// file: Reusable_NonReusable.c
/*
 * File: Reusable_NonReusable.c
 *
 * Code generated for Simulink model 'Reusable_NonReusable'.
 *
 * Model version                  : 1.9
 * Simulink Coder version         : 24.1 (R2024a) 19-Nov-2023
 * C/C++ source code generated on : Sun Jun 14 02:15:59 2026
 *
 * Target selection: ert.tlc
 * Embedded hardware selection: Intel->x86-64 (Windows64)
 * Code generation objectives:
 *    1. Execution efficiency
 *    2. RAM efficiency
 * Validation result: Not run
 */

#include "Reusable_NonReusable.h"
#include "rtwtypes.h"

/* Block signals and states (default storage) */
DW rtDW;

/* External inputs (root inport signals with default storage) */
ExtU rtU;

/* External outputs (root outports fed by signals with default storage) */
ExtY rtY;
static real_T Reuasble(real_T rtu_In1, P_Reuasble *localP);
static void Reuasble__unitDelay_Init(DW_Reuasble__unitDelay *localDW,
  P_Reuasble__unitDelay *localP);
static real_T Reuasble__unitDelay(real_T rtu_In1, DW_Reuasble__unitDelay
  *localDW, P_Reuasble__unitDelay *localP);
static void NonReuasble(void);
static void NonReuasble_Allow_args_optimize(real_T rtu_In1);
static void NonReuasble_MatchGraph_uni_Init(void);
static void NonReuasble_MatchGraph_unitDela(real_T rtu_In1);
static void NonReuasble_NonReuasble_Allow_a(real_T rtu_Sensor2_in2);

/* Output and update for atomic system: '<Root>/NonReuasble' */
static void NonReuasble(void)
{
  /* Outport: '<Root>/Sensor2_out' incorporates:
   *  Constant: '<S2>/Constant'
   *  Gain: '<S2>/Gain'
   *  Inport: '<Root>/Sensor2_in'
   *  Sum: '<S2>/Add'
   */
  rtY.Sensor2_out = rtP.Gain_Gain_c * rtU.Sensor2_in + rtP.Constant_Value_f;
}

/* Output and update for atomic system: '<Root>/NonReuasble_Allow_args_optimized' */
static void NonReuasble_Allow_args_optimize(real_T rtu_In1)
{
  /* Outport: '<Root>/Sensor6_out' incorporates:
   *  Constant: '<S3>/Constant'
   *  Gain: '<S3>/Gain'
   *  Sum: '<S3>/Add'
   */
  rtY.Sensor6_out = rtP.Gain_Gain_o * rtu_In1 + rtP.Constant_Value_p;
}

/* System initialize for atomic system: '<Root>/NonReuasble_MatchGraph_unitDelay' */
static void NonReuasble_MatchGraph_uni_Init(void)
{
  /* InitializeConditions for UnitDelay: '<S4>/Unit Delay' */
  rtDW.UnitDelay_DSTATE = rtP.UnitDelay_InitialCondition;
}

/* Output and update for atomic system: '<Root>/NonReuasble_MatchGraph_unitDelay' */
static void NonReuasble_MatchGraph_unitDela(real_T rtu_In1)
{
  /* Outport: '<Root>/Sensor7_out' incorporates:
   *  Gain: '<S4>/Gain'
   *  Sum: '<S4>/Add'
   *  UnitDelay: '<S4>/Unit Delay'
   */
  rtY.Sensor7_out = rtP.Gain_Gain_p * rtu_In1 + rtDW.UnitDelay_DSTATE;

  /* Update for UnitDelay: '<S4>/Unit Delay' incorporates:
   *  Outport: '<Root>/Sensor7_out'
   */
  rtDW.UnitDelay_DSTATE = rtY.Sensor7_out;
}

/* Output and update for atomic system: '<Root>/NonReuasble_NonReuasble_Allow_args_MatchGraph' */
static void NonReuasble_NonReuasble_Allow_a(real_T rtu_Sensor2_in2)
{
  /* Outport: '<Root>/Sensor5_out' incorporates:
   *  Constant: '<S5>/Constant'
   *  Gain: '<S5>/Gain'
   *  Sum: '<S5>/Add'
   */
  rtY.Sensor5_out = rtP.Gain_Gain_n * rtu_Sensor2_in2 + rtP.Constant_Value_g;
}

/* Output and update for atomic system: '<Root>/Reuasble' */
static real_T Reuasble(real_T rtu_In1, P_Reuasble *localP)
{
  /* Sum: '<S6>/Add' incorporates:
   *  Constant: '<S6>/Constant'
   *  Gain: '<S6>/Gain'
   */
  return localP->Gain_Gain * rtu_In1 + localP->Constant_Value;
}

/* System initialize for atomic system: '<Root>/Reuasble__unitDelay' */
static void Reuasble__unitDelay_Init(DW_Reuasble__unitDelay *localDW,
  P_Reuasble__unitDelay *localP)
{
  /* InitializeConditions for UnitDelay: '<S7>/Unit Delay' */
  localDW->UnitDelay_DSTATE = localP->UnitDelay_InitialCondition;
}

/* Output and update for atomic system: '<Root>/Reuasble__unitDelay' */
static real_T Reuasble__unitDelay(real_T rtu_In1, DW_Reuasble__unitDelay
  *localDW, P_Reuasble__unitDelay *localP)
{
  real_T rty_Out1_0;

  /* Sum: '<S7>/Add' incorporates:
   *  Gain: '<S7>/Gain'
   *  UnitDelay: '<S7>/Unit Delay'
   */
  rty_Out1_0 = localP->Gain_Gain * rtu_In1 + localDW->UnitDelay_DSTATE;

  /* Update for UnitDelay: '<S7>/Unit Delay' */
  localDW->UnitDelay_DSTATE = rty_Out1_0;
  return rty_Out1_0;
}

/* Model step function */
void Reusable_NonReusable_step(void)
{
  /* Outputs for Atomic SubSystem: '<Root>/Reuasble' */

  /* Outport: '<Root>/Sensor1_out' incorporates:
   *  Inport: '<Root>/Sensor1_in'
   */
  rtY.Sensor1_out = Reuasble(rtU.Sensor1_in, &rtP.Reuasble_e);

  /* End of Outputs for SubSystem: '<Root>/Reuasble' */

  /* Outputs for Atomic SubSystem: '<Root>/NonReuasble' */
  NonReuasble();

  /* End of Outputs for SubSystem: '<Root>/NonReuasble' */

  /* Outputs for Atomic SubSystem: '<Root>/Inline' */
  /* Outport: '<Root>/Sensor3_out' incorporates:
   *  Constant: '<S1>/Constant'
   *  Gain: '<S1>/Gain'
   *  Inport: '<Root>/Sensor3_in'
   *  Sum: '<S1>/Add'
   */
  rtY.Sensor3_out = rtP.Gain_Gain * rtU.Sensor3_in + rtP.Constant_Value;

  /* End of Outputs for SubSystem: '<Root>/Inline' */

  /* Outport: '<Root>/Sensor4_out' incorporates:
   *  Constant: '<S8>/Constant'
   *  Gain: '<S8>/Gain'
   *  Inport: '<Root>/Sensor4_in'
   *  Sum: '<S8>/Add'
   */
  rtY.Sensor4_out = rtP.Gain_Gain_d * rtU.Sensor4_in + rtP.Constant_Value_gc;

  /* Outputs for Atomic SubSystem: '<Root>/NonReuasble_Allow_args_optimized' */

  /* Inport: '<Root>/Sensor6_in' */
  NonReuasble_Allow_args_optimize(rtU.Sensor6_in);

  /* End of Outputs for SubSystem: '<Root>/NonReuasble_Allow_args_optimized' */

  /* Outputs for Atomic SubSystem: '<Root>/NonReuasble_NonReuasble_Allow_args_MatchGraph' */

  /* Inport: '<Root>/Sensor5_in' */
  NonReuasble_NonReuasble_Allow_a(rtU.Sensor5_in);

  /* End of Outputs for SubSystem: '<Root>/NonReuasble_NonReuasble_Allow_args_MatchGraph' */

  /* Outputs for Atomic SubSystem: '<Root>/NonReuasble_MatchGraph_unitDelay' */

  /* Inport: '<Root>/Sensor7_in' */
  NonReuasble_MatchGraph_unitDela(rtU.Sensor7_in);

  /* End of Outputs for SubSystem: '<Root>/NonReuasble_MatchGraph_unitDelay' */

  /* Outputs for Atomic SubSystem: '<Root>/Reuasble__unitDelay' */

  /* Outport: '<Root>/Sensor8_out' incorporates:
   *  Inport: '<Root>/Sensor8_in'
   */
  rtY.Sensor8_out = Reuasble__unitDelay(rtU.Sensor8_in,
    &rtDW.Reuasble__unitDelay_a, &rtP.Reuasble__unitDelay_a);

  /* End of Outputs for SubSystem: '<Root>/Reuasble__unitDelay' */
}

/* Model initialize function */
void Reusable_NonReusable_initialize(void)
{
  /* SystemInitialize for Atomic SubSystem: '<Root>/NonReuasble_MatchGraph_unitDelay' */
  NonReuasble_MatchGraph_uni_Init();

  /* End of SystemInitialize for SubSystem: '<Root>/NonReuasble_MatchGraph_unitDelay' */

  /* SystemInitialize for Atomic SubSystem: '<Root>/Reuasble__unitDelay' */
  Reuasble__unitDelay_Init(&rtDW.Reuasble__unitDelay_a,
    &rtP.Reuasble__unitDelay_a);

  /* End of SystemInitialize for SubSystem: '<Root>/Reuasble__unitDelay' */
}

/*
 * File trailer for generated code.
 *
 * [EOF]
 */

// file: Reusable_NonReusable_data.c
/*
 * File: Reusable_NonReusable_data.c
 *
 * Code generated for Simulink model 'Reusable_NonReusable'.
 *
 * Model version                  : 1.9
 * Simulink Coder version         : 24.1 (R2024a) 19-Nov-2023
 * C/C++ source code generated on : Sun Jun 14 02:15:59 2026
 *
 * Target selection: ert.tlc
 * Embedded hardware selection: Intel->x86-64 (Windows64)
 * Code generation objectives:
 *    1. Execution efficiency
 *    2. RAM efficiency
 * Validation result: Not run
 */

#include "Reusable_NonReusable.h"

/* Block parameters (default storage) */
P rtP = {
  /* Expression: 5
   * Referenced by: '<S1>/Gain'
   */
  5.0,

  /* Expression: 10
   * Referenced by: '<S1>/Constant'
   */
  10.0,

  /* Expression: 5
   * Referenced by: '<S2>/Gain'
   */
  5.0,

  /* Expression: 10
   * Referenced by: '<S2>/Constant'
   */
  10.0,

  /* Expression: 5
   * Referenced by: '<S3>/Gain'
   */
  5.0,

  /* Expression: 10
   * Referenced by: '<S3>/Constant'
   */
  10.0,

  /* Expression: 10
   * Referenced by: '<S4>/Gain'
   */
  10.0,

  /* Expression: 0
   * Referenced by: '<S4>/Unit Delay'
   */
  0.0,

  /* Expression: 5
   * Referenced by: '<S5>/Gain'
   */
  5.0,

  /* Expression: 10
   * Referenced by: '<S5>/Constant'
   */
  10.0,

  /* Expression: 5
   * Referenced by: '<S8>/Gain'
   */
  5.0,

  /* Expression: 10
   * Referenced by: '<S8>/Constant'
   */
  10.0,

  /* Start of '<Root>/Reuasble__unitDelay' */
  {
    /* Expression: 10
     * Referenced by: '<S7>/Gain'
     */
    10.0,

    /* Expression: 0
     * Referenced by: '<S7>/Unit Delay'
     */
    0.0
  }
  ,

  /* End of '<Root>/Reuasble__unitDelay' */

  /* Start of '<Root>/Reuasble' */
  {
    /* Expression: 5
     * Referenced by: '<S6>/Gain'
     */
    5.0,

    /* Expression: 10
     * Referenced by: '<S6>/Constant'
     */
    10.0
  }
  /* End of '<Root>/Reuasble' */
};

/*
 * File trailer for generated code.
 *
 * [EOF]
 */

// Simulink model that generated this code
simulink model "Reusable_NonReusable"  (R2024a)
settings: Solver=FixedStepDiscrete  StartTime=0.0  StopTime=10.0  FixedStep=1  RelTol=1e-3
model workspace (MAT data in the model file):
  Kp : Simulink.Parameter (value not decoded)

== system Reusable_NonReusable ==
  Sensor1_in : Inport
  Sensor2_in : Inport  Port=2
  Sensor3_in : Inport  Port=3
  Sensor4_in : Inport  Port=4
  Sensor6_in : Inport  Port=5
  Sensor5_in : Inport  Port=6
  Sensor7_in : Inport  Port=7
  Sensor8_in : Inport  Port=8
  Inline : Subsystem  TreatAsAtomicUnit=on
  NonReuasble : Subsystem  TreatAsAtomicUnit=on
  NonReuasble_Allow_args_optimized : Subsystem  TreatAsAtomicUnit=on
  NonReuasble_MatchGraph_unitDelay : Subsystem  TreatAsAtomicUnit=on
  NonReuasble_NonReuasble_Allow_args_MatchGraph : Subsystem  TreatAsAtomicUnit=on
  Reuasble : Subsystem  TreatAsAtomicUnit=on
  Reuasble__unitDelay : Subsystem  TreatAsAtomicUnit=on
  Virtual : Subsystem
  Sensor1_out : Outport
  Sensor2_out : Outport  Port=2
  Sensor3_out : Outport  Port=3
  Sensor4_out : Outport  Port=4
  Sensor6_out : Outport  Port=5
  Sensor5_out : Outport  Port=6
  Sensor7_out : Outport  Port=7
  Sensor8_out : Outport  Port=8
  wires:
  Sensor1_in/1 -> Reuasble/1(In1)
  Reuasble/1(Out1) -> Sensor1_out/1
  NonReuasble/1(Out1) -> Sensor2_out/1
  Inline/1(Out1) -> Sensor3_out/1
  Sensor3_in/1 -> Inline/1(In1)
  Sensor4_in/1 -> Virtual/1(In1)  "Sensor4_in"
  Virtual/1(Out1) -> Sensor4_out/1
  Sensor5_in/1 -> NonReuasble_NonReuasble_Allow_args_MatchGraph/1(Sensor2_in2)
  Sensor8_in/1 -> Reuasble__unitDelay/1(In1)
  Sensor2_in/1 -> NonReuasble/1(Sensor2_in)
  Sensor6_in/1 -> NonReuasble_Allow_args_optimized/1(In1)
  NonReuasble_NonReuasble_Allow_args_MatchGraph/1(Out1) -> Sensor5_out/1
  NonReuasble_Allow_args_optimized/1(Sensor2_out1) -> Sensor6_out/1
  Reuasble__unitDelay/1(Out1) -> Sensor8_out/1
  Sensor7_in/1 -> NonReuasble_MatchGraph_unitDelay/1(In1)
  NonReuasble_MatchGraph_unitDelay/1(out1) -> Sensor7_out/1

== system Reusable_NonReusable/Inline ==
  In1 : Inport
  Add : Sum
  Constant : Constant  Value=10
  Gain : Gain  Gain=5
  Out1 : Outport
  wires:
  Add/1 -> Out1/1
  Constant/1 -> Add/2
  In1/1 -> Gain/1
  Gain/1 -> Add/1

== system Reusable_NonReusable/NonReuasble ==
  Sensor2_in : Inport
  Add : Sum
  Constant : Constant  Value=10
  Gain : Gain  Gain=5
  Out1 : Outport
  wires:
  Add/1 -> Out1/1
  Constant/1 -> Add/2
  Sensor2_in/1 -> Gain/1
  Gain/1 -> Add/1

== system Reusable_NonReusable/NonReuasble_Allow_args_optimized ==
  In1 : Inport
  Add : Sum
  Constant : Constant  Value=10
  Gain : Gain  Gain=5
  Sensor2_out1 : Outport
  wires:
  Gain/1 -> Add/1
  In1/1 -> Gain/1
  Constant/1 -> Add/2
  Add/1 -> Sensor2_out1/1

== system Reusable_NonReusable/NonReuasble_MatchGraph_unitDelay ==
  In1 : Inport
  Add : Sum
  Gain : Gain  Gain=10
  Unit Delay : UnitDelay  SampleTime=-1  HasFrameUpgradeWarning=on
  out1 : Outport
  wires:
  Gain/1 -> Add/1
  In1/1 -> Gain/1
  Unit Delay/1 -> Add/2
  Add/1 -> Unit Delay/1, out1/1

== system Reusable_NonReusable/NonReuasble_NonReuasble_Allow_args_MatchGraph ==
  Sensor2_in2 : Inport
  Add : Sum
  Constant : Constant  Value=10
  Gain : Gain  Gain=5
  Out1 : Outport
  wires:
  Add/1 -> Out1/1
  Constant/1 -> Add/2
  Sensor2_in2/1 -> Gain/1
  Gain/1 -> Add/1

== system Reusable_NonReusable/Reuasble ==
  In1 : Inport
  Add : Sum
  Constant : Constant  Value=10
  Gain : Gain  Gain=5
  Out1 : Outport
  wires:
  Gain/1 -> Add/1
  In1/1 -> Gain/1
  Constant/1 -> Add/2
  Add/1 -> Out1/1

== system Reusable_NonReusable/Reuasble__unitDelay ==
  In1 : Inport
  Add : Sum
  Gain : Gain  Gain=10
  Unit Delay : UnitDelay  SampleTime=-1  HasFrameUpgradeWarning=on
  Out1 : Outport
  wires:
  Add/1 -> Out1/1, Unit Delay/1
  Unit Delay/1 -> Add/2
  In1/1 -> Gain/1
  Gain/1 -> Add/1

== system Reusable_NonReusable/Virtual ==
  In1 : Inport
  Add : Sum
  Constant : Constant  Value=10
  Gain : Gain  Gain=5
  Out1 : Outport
  wires:
  Gain/1 -> Add/1
  In1/1 -> Gain/1
  Constant/1 -> Add/2
  Add/1 -> Out1/1
